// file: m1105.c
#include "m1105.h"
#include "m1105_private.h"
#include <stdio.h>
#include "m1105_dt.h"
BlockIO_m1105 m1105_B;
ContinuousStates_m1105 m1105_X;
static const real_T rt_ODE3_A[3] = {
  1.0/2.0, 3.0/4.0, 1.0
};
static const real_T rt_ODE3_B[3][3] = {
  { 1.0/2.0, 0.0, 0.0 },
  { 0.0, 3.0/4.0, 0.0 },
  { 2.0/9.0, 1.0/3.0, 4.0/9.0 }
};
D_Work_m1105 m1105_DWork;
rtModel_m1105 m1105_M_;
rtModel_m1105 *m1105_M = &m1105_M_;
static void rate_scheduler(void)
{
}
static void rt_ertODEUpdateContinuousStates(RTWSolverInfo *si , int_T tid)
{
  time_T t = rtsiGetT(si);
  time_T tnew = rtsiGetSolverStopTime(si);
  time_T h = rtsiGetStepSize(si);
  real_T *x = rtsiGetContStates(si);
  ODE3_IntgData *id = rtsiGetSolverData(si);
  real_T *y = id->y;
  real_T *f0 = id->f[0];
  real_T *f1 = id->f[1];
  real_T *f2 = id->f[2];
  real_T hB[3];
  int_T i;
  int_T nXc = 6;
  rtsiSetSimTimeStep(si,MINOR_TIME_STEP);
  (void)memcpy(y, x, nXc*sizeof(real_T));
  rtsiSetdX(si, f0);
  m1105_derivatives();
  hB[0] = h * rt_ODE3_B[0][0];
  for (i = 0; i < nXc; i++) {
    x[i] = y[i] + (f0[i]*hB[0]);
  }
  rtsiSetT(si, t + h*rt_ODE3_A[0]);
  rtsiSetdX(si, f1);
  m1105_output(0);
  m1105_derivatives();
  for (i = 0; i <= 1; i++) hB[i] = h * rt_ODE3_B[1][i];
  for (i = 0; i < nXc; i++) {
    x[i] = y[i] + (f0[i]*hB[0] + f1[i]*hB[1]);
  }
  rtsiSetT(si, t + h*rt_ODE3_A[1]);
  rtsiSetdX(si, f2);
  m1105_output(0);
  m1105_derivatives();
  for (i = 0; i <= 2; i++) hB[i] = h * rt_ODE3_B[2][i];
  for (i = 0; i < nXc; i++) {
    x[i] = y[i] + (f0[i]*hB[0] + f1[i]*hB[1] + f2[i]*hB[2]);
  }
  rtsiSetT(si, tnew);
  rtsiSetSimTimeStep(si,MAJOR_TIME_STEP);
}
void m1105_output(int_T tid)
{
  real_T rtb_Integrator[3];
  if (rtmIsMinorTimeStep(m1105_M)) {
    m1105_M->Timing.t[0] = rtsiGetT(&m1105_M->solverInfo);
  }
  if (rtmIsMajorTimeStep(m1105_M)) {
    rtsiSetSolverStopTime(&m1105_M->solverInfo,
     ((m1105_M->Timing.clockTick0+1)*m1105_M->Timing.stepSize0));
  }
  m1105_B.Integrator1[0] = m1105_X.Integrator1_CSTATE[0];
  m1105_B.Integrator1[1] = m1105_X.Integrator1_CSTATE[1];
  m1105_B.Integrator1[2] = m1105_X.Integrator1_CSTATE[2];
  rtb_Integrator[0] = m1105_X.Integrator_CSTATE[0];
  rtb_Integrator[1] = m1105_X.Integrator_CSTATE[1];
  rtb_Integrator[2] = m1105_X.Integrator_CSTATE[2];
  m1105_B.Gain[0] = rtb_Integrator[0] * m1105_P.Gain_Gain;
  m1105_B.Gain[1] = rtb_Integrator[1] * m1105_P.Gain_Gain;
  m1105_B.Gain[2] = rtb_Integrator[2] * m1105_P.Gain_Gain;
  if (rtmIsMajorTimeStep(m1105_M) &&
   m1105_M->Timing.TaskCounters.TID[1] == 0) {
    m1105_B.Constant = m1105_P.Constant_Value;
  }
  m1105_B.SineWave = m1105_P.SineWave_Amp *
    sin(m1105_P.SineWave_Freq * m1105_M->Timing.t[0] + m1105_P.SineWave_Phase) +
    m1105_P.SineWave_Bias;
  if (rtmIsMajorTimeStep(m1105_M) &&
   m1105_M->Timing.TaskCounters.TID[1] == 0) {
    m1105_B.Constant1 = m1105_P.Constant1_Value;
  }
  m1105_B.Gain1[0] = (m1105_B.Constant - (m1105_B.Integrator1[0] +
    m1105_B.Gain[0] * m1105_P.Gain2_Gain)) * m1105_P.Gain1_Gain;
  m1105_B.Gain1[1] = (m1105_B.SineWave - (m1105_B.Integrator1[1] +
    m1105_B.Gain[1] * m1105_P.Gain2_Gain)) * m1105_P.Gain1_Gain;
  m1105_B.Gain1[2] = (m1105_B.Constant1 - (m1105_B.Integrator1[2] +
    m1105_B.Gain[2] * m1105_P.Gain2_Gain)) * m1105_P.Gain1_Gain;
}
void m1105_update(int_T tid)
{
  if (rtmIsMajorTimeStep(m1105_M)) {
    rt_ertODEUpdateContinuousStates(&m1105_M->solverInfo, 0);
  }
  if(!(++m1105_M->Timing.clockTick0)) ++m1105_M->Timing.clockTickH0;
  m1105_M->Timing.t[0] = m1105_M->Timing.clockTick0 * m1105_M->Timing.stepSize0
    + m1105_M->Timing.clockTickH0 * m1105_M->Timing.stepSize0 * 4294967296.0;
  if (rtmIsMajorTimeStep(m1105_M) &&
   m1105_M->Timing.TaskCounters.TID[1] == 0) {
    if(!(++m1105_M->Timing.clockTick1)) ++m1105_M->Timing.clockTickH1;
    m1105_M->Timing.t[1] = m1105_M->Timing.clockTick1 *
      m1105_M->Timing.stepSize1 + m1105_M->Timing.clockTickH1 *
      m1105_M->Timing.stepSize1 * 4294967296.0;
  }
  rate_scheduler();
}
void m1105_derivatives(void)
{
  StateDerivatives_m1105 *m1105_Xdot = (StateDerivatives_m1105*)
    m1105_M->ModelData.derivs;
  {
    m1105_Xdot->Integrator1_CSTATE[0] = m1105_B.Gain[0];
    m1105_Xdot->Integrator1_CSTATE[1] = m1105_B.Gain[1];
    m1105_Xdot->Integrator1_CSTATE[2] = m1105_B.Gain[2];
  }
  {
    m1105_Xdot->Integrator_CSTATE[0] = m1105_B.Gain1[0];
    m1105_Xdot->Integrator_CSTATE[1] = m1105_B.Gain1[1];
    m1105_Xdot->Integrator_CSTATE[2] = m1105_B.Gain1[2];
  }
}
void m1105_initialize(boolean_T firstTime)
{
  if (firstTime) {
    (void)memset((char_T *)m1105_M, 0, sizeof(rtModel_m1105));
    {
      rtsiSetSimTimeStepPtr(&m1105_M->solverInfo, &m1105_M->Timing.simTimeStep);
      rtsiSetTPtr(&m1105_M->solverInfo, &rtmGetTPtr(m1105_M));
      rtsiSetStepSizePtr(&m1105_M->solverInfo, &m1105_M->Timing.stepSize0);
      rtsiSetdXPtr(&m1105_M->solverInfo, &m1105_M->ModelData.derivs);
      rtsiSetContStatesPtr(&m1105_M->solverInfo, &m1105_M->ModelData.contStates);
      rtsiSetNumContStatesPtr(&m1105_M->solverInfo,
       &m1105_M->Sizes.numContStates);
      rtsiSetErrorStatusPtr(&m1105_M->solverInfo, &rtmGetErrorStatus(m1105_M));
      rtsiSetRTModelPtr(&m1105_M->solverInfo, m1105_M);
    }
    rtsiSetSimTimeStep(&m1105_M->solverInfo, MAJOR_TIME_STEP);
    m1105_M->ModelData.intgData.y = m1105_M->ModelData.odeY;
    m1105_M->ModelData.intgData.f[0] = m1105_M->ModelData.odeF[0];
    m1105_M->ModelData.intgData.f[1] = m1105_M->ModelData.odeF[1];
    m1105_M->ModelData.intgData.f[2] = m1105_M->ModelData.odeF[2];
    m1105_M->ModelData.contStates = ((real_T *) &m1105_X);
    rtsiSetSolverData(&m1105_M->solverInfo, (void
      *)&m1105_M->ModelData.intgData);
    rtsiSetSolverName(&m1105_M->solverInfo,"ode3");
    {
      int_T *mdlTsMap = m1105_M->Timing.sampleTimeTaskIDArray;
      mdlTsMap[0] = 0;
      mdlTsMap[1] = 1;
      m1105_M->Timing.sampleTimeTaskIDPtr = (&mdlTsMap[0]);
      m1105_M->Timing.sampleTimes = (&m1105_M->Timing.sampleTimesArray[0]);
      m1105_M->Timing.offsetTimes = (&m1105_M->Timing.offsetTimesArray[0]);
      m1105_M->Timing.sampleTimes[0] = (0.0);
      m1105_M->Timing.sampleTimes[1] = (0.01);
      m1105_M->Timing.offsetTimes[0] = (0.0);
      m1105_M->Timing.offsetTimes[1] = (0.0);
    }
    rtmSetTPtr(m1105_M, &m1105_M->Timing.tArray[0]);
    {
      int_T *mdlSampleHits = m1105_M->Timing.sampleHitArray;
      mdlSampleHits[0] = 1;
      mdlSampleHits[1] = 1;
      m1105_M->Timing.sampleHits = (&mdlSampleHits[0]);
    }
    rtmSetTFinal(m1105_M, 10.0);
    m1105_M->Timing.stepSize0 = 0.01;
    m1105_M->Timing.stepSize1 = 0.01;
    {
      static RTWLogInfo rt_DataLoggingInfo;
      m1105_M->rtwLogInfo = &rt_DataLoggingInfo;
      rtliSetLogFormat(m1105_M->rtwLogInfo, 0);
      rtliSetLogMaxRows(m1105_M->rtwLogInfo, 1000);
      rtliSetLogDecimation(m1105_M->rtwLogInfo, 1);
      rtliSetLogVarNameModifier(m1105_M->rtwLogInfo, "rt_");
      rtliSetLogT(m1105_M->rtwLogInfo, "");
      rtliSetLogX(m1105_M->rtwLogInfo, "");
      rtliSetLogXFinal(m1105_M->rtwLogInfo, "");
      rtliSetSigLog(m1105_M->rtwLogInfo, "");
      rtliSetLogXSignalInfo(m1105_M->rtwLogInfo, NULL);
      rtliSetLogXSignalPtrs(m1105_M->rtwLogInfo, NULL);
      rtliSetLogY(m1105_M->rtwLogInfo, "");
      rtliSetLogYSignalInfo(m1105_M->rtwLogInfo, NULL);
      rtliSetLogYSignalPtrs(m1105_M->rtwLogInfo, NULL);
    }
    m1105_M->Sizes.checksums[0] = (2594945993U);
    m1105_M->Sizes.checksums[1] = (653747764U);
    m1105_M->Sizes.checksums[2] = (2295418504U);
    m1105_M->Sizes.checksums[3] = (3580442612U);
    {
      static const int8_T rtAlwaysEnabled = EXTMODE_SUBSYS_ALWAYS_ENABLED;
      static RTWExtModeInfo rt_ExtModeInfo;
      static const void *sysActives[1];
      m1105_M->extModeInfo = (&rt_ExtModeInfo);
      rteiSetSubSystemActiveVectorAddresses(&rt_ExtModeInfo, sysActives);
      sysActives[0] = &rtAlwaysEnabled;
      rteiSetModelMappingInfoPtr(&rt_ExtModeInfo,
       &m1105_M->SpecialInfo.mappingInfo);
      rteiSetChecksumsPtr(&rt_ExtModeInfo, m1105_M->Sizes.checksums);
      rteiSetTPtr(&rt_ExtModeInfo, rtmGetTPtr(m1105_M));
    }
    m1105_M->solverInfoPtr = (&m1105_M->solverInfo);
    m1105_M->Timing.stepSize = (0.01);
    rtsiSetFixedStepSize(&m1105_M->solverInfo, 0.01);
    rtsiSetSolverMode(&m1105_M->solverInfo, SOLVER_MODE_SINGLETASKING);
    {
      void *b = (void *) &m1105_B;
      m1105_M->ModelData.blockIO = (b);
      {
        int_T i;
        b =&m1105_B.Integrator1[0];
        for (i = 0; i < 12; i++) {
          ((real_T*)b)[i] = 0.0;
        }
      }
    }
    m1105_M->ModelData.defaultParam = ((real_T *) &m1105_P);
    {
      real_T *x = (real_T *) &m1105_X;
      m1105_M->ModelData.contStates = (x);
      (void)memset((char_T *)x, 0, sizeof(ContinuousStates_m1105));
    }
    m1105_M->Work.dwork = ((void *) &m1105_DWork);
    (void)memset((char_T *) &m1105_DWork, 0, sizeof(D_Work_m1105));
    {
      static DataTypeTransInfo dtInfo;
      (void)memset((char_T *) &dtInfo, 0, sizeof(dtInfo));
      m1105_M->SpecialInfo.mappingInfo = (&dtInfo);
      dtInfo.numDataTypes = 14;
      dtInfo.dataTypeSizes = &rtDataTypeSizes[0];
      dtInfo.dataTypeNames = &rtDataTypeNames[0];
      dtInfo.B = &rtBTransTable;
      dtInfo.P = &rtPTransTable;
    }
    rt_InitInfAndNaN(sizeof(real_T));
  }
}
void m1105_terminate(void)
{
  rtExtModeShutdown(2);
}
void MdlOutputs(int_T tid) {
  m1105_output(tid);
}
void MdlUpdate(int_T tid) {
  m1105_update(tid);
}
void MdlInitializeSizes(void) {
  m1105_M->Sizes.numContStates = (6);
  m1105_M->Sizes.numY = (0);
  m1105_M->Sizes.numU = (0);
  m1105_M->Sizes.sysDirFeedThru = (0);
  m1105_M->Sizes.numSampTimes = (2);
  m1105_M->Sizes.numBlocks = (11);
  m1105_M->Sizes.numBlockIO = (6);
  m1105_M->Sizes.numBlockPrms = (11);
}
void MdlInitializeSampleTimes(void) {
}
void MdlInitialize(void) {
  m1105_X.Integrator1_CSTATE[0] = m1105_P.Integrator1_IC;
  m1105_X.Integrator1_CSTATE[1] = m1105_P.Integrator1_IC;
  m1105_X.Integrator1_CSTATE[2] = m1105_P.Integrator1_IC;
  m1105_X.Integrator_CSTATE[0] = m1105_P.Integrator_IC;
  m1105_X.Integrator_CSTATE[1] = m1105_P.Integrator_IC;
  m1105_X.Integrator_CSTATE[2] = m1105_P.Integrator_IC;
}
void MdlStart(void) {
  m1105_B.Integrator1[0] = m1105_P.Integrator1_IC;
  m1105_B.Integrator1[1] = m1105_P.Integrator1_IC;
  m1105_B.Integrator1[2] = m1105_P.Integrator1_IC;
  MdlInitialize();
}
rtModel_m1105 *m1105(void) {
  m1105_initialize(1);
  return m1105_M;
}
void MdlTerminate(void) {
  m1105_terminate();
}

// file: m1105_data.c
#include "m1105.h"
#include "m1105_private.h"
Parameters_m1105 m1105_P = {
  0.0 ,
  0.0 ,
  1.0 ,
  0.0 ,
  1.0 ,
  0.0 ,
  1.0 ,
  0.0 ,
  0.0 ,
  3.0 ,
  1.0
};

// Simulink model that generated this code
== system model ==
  Integrator1 : Integrator  <- 1: Gain
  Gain : Gain  <- 1: Integrator
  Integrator : Integrator  <- 1: Gain1
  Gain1 : Gain  <- 1: Sum#1
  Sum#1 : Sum  Inputs=-+  <- 1: Sum#2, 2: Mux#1
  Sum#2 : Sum  Inputs=++  <- 1: Integrator1, 2: Gain2
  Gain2 : Gain  Gain=3  <- 1: Gain
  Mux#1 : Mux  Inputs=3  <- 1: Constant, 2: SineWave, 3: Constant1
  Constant : Constant  Value=0
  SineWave : Sin
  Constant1 : Constant  Value=0
